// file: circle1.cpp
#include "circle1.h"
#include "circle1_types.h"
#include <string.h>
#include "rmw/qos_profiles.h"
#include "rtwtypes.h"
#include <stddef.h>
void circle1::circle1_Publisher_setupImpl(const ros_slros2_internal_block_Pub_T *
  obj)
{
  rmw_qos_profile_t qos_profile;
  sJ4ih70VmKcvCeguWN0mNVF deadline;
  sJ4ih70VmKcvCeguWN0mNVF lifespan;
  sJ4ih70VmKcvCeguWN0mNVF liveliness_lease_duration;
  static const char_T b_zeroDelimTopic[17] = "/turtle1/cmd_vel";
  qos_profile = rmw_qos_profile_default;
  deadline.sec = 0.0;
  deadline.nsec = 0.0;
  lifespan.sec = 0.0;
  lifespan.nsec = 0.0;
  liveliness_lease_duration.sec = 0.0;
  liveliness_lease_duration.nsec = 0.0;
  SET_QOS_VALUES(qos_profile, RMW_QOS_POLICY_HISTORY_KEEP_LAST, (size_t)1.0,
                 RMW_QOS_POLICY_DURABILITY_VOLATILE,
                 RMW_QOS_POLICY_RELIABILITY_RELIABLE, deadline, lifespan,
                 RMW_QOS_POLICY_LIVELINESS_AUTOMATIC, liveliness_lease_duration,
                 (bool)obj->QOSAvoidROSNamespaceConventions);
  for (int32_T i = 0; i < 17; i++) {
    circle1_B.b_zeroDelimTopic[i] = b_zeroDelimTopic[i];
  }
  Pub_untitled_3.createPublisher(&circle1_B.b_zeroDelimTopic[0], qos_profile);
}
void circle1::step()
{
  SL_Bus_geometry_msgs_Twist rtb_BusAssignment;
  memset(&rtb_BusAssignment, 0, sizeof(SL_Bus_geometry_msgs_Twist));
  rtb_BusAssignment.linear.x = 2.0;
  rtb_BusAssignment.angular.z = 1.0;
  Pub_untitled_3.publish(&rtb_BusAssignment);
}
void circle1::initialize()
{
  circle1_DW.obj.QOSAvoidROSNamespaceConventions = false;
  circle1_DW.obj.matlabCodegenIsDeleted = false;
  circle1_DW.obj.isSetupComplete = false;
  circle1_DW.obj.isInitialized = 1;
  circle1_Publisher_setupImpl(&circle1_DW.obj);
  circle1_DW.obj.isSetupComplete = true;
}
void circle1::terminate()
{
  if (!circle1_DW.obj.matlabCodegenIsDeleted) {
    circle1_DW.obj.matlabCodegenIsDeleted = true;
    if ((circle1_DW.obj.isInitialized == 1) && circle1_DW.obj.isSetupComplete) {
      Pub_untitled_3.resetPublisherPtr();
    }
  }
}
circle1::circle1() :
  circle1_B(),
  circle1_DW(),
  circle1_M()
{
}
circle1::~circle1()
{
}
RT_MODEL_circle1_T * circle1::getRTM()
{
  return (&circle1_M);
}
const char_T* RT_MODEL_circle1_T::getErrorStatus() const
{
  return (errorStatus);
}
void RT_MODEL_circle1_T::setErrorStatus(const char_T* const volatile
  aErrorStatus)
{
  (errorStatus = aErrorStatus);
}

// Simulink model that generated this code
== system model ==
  Publish#1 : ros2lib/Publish  <- 1: BusAssignment
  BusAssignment : BusAssignment  <- 1: BlankMessage#1, 2: Constant#1, 3: Constant#2
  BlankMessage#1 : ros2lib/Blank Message
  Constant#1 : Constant  Value=2
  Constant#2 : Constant
